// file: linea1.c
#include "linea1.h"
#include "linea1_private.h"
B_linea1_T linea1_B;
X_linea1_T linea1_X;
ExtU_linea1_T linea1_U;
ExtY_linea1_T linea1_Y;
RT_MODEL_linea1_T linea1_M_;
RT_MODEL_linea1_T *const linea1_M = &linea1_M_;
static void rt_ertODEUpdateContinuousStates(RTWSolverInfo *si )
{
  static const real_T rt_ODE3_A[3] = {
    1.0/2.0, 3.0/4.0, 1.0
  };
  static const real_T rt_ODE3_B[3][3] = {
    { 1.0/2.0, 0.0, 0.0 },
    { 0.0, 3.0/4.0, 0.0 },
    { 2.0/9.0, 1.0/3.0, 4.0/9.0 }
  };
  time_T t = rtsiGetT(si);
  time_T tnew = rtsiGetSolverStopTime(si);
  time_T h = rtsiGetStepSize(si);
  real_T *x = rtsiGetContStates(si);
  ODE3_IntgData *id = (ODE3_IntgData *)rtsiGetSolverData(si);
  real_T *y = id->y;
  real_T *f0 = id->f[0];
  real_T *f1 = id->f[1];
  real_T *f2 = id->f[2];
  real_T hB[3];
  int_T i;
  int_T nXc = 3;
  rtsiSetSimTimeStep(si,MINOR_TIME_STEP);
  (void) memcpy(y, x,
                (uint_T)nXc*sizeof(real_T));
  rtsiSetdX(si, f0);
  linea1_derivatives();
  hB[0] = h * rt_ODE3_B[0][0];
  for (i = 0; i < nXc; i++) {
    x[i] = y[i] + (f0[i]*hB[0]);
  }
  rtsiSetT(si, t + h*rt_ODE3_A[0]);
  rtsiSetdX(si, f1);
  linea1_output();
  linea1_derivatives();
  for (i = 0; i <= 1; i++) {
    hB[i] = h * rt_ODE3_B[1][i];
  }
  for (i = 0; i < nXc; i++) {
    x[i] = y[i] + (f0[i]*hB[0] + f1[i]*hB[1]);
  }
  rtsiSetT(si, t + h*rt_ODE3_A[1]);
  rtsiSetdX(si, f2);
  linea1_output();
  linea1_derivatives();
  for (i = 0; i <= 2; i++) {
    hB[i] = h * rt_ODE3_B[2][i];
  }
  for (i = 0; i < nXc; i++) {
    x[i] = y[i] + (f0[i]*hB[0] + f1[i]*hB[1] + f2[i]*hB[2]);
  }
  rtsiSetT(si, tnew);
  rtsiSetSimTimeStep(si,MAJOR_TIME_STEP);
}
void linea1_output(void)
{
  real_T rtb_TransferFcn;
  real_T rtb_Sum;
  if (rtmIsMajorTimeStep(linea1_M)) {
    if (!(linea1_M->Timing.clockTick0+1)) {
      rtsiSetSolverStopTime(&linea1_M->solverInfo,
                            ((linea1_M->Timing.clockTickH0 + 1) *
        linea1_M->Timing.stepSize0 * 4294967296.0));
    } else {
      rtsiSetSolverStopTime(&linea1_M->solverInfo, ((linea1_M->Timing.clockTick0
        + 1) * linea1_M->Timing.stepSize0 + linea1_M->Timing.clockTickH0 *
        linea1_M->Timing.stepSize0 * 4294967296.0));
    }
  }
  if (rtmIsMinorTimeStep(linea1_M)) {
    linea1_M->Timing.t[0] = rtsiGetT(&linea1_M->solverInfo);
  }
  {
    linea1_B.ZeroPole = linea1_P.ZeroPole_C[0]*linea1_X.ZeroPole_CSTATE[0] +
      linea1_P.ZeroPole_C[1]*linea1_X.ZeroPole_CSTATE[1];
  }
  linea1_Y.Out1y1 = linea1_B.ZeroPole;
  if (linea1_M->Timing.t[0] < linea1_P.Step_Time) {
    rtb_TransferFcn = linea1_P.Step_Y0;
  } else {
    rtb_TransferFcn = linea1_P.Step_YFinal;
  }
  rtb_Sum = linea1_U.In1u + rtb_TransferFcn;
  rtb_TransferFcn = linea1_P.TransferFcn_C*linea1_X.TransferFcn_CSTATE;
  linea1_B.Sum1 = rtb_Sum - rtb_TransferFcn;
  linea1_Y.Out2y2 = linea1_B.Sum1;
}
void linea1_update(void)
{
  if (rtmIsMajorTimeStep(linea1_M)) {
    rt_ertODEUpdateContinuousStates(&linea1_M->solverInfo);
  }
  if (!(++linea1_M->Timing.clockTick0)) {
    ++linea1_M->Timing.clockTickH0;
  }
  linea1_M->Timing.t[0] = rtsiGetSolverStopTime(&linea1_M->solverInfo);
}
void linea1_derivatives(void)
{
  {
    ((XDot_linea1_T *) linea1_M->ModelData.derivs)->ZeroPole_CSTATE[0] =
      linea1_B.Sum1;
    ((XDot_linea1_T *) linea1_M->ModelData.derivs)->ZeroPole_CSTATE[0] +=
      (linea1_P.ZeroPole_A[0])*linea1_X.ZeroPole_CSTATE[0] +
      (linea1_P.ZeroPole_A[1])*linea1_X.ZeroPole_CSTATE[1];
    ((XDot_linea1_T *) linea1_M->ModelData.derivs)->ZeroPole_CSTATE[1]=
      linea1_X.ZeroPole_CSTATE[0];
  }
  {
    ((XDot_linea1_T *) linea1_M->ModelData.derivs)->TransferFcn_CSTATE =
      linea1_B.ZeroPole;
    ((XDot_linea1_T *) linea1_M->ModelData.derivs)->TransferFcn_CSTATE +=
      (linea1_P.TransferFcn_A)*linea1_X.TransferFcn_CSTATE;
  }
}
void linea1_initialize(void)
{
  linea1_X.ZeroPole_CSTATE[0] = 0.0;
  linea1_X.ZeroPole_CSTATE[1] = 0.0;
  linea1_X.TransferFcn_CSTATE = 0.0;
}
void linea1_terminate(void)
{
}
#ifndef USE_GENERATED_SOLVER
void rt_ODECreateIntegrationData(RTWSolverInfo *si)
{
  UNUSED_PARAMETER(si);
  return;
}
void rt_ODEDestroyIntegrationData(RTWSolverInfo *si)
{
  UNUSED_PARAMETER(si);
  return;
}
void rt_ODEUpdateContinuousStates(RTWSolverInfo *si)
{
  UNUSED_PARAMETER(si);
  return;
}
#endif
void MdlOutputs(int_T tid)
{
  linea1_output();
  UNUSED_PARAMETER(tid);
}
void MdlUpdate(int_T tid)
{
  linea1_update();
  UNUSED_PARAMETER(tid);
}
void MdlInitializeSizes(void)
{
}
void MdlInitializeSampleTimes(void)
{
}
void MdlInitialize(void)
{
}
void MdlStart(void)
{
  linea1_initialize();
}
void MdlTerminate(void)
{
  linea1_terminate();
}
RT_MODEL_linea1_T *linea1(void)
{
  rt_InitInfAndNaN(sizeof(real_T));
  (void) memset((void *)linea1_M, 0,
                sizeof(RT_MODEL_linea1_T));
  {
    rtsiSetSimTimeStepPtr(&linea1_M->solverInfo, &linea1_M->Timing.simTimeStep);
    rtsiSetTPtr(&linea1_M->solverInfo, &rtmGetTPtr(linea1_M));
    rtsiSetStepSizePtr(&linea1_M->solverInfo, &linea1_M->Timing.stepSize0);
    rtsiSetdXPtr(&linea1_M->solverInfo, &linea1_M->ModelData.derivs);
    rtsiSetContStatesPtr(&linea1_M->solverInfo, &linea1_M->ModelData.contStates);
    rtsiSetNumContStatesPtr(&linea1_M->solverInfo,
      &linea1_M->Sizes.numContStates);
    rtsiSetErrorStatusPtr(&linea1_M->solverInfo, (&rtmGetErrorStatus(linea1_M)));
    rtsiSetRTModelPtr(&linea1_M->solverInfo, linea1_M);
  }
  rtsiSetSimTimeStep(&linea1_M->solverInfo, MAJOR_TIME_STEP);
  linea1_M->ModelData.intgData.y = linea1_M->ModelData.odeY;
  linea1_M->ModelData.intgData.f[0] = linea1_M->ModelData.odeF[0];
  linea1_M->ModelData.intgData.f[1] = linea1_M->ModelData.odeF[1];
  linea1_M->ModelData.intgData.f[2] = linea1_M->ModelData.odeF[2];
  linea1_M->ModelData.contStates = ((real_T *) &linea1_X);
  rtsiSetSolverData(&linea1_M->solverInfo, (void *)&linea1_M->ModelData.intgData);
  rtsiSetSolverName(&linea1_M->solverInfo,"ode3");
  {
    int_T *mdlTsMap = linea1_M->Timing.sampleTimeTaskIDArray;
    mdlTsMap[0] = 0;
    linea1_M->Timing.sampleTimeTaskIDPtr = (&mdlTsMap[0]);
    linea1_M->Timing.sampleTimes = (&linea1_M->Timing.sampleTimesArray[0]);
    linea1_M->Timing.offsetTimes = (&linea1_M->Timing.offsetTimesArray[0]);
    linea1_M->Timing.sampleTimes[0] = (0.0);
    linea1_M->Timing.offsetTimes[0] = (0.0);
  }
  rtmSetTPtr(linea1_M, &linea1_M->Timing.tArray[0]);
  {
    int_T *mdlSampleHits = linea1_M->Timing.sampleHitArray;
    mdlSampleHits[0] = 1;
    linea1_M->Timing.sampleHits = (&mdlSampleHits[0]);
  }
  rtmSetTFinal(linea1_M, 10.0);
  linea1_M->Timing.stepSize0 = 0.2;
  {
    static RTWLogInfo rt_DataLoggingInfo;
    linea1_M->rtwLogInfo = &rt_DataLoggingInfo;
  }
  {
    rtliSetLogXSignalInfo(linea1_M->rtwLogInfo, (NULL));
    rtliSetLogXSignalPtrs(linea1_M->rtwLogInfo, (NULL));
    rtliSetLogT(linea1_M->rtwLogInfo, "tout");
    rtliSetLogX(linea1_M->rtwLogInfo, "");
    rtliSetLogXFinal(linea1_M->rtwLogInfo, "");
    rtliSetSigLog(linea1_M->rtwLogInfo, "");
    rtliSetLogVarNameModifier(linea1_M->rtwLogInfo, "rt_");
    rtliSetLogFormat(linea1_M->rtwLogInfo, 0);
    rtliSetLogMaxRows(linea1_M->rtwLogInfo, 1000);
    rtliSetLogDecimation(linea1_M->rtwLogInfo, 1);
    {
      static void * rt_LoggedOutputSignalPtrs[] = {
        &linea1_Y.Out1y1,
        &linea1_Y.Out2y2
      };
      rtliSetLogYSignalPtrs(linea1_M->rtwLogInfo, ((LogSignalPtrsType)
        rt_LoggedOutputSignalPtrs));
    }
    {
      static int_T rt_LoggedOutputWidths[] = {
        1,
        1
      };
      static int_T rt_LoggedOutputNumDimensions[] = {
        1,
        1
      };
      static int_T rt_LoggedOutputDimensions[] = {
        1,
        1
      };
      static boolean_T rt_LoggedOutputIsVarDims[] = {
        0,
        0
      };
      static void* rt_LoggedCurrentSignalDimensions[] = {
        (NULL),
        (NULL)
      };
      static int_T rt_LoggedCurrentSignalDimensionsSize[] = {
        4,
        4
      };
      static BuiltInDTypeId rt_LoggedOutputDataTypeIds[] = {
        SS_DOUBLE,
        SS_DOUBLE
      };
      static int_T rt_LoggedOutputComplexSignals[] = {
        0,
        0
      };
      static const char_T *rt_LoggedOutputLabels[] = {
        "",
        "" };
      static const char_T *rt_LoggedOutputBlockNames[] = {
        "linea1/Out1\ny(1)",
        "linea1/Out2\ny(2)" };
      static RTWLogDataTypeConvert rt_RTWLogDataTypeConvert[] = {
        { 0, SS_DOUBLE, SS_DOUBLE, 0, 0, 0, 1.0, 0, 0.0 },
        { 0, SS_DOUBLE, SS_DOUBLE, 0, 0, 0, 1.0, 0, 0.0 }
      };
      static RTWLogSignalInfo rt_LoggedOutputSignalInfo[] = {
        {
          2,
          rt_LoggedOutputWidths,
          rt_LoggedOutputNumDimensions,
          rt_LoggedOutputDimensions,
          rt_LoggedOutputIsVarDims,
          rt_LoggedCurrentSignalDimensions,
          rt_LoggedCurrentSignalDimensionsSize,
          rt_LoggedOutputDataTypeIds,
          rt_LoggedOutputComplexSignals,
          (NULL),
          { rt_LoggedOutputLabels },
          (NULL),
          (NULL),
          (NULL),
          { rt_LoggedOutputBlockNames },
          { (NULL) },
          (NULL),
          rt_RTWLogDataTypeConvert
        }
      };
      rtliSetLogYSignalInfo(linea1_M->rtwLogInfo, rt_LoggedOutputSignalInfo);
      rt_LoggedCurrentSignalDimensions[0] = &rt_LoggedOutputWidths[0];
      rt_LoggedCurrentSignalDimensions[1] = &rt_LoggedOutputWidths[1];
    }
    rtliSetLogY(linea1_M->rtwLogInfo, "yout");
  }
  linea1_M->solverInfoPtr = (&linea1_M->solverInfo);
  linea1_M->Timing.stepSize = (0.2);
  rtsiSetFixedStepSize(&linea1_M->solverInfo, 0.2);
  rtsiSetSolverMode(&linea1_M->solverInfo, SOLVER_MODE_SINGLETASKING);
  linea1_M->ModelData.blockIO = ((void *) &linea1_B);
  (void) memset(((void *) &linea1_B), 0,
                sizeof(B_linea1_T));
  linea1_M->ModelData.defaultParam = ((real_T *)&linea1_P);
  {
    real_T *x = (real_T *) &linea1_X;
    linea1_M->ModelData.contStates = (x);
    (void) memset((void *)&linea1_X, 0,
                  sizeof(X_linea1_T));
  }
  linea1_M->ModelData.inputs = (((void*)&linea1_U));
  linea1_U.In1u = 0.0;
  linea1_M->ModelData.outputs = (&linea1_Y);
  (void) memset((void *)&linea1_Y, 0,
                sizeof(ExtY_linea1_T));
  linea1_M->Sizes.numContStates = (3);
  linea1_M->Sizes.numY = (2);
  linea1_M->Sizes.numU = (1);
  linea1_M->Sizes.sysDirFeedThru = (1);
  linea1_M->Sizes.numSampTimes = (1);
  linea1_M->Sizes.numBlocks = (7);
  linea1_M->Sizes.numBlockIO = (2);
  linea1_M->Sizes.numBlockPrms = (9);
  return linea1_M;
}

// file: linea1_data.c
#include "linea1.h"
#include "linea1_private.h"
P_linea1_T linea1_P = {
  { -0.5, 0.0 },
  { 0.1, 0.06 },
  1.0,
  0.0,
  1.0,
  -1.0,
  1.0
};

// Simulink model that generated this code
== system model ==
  In1u : Inport
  Out1y1 : Outport  <- 1: ZeroPole
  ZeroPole : ZeroPole  Gain=[0.1]  <- 1: Sum1
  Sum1 : Sum  Inputs=+-  <- 1: Sum, 2: TransferFcn
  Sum : Sum  Inputs=++  <- 1: In1u, 2: Step
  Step : Step  Time=1  Before=0  After=1
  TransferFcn : TransferFcn  Numerator=[1]  Denominator=[1 1]  <- 1: ZeroPole
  Out2y2 : Outport  <- 1: Sum1
